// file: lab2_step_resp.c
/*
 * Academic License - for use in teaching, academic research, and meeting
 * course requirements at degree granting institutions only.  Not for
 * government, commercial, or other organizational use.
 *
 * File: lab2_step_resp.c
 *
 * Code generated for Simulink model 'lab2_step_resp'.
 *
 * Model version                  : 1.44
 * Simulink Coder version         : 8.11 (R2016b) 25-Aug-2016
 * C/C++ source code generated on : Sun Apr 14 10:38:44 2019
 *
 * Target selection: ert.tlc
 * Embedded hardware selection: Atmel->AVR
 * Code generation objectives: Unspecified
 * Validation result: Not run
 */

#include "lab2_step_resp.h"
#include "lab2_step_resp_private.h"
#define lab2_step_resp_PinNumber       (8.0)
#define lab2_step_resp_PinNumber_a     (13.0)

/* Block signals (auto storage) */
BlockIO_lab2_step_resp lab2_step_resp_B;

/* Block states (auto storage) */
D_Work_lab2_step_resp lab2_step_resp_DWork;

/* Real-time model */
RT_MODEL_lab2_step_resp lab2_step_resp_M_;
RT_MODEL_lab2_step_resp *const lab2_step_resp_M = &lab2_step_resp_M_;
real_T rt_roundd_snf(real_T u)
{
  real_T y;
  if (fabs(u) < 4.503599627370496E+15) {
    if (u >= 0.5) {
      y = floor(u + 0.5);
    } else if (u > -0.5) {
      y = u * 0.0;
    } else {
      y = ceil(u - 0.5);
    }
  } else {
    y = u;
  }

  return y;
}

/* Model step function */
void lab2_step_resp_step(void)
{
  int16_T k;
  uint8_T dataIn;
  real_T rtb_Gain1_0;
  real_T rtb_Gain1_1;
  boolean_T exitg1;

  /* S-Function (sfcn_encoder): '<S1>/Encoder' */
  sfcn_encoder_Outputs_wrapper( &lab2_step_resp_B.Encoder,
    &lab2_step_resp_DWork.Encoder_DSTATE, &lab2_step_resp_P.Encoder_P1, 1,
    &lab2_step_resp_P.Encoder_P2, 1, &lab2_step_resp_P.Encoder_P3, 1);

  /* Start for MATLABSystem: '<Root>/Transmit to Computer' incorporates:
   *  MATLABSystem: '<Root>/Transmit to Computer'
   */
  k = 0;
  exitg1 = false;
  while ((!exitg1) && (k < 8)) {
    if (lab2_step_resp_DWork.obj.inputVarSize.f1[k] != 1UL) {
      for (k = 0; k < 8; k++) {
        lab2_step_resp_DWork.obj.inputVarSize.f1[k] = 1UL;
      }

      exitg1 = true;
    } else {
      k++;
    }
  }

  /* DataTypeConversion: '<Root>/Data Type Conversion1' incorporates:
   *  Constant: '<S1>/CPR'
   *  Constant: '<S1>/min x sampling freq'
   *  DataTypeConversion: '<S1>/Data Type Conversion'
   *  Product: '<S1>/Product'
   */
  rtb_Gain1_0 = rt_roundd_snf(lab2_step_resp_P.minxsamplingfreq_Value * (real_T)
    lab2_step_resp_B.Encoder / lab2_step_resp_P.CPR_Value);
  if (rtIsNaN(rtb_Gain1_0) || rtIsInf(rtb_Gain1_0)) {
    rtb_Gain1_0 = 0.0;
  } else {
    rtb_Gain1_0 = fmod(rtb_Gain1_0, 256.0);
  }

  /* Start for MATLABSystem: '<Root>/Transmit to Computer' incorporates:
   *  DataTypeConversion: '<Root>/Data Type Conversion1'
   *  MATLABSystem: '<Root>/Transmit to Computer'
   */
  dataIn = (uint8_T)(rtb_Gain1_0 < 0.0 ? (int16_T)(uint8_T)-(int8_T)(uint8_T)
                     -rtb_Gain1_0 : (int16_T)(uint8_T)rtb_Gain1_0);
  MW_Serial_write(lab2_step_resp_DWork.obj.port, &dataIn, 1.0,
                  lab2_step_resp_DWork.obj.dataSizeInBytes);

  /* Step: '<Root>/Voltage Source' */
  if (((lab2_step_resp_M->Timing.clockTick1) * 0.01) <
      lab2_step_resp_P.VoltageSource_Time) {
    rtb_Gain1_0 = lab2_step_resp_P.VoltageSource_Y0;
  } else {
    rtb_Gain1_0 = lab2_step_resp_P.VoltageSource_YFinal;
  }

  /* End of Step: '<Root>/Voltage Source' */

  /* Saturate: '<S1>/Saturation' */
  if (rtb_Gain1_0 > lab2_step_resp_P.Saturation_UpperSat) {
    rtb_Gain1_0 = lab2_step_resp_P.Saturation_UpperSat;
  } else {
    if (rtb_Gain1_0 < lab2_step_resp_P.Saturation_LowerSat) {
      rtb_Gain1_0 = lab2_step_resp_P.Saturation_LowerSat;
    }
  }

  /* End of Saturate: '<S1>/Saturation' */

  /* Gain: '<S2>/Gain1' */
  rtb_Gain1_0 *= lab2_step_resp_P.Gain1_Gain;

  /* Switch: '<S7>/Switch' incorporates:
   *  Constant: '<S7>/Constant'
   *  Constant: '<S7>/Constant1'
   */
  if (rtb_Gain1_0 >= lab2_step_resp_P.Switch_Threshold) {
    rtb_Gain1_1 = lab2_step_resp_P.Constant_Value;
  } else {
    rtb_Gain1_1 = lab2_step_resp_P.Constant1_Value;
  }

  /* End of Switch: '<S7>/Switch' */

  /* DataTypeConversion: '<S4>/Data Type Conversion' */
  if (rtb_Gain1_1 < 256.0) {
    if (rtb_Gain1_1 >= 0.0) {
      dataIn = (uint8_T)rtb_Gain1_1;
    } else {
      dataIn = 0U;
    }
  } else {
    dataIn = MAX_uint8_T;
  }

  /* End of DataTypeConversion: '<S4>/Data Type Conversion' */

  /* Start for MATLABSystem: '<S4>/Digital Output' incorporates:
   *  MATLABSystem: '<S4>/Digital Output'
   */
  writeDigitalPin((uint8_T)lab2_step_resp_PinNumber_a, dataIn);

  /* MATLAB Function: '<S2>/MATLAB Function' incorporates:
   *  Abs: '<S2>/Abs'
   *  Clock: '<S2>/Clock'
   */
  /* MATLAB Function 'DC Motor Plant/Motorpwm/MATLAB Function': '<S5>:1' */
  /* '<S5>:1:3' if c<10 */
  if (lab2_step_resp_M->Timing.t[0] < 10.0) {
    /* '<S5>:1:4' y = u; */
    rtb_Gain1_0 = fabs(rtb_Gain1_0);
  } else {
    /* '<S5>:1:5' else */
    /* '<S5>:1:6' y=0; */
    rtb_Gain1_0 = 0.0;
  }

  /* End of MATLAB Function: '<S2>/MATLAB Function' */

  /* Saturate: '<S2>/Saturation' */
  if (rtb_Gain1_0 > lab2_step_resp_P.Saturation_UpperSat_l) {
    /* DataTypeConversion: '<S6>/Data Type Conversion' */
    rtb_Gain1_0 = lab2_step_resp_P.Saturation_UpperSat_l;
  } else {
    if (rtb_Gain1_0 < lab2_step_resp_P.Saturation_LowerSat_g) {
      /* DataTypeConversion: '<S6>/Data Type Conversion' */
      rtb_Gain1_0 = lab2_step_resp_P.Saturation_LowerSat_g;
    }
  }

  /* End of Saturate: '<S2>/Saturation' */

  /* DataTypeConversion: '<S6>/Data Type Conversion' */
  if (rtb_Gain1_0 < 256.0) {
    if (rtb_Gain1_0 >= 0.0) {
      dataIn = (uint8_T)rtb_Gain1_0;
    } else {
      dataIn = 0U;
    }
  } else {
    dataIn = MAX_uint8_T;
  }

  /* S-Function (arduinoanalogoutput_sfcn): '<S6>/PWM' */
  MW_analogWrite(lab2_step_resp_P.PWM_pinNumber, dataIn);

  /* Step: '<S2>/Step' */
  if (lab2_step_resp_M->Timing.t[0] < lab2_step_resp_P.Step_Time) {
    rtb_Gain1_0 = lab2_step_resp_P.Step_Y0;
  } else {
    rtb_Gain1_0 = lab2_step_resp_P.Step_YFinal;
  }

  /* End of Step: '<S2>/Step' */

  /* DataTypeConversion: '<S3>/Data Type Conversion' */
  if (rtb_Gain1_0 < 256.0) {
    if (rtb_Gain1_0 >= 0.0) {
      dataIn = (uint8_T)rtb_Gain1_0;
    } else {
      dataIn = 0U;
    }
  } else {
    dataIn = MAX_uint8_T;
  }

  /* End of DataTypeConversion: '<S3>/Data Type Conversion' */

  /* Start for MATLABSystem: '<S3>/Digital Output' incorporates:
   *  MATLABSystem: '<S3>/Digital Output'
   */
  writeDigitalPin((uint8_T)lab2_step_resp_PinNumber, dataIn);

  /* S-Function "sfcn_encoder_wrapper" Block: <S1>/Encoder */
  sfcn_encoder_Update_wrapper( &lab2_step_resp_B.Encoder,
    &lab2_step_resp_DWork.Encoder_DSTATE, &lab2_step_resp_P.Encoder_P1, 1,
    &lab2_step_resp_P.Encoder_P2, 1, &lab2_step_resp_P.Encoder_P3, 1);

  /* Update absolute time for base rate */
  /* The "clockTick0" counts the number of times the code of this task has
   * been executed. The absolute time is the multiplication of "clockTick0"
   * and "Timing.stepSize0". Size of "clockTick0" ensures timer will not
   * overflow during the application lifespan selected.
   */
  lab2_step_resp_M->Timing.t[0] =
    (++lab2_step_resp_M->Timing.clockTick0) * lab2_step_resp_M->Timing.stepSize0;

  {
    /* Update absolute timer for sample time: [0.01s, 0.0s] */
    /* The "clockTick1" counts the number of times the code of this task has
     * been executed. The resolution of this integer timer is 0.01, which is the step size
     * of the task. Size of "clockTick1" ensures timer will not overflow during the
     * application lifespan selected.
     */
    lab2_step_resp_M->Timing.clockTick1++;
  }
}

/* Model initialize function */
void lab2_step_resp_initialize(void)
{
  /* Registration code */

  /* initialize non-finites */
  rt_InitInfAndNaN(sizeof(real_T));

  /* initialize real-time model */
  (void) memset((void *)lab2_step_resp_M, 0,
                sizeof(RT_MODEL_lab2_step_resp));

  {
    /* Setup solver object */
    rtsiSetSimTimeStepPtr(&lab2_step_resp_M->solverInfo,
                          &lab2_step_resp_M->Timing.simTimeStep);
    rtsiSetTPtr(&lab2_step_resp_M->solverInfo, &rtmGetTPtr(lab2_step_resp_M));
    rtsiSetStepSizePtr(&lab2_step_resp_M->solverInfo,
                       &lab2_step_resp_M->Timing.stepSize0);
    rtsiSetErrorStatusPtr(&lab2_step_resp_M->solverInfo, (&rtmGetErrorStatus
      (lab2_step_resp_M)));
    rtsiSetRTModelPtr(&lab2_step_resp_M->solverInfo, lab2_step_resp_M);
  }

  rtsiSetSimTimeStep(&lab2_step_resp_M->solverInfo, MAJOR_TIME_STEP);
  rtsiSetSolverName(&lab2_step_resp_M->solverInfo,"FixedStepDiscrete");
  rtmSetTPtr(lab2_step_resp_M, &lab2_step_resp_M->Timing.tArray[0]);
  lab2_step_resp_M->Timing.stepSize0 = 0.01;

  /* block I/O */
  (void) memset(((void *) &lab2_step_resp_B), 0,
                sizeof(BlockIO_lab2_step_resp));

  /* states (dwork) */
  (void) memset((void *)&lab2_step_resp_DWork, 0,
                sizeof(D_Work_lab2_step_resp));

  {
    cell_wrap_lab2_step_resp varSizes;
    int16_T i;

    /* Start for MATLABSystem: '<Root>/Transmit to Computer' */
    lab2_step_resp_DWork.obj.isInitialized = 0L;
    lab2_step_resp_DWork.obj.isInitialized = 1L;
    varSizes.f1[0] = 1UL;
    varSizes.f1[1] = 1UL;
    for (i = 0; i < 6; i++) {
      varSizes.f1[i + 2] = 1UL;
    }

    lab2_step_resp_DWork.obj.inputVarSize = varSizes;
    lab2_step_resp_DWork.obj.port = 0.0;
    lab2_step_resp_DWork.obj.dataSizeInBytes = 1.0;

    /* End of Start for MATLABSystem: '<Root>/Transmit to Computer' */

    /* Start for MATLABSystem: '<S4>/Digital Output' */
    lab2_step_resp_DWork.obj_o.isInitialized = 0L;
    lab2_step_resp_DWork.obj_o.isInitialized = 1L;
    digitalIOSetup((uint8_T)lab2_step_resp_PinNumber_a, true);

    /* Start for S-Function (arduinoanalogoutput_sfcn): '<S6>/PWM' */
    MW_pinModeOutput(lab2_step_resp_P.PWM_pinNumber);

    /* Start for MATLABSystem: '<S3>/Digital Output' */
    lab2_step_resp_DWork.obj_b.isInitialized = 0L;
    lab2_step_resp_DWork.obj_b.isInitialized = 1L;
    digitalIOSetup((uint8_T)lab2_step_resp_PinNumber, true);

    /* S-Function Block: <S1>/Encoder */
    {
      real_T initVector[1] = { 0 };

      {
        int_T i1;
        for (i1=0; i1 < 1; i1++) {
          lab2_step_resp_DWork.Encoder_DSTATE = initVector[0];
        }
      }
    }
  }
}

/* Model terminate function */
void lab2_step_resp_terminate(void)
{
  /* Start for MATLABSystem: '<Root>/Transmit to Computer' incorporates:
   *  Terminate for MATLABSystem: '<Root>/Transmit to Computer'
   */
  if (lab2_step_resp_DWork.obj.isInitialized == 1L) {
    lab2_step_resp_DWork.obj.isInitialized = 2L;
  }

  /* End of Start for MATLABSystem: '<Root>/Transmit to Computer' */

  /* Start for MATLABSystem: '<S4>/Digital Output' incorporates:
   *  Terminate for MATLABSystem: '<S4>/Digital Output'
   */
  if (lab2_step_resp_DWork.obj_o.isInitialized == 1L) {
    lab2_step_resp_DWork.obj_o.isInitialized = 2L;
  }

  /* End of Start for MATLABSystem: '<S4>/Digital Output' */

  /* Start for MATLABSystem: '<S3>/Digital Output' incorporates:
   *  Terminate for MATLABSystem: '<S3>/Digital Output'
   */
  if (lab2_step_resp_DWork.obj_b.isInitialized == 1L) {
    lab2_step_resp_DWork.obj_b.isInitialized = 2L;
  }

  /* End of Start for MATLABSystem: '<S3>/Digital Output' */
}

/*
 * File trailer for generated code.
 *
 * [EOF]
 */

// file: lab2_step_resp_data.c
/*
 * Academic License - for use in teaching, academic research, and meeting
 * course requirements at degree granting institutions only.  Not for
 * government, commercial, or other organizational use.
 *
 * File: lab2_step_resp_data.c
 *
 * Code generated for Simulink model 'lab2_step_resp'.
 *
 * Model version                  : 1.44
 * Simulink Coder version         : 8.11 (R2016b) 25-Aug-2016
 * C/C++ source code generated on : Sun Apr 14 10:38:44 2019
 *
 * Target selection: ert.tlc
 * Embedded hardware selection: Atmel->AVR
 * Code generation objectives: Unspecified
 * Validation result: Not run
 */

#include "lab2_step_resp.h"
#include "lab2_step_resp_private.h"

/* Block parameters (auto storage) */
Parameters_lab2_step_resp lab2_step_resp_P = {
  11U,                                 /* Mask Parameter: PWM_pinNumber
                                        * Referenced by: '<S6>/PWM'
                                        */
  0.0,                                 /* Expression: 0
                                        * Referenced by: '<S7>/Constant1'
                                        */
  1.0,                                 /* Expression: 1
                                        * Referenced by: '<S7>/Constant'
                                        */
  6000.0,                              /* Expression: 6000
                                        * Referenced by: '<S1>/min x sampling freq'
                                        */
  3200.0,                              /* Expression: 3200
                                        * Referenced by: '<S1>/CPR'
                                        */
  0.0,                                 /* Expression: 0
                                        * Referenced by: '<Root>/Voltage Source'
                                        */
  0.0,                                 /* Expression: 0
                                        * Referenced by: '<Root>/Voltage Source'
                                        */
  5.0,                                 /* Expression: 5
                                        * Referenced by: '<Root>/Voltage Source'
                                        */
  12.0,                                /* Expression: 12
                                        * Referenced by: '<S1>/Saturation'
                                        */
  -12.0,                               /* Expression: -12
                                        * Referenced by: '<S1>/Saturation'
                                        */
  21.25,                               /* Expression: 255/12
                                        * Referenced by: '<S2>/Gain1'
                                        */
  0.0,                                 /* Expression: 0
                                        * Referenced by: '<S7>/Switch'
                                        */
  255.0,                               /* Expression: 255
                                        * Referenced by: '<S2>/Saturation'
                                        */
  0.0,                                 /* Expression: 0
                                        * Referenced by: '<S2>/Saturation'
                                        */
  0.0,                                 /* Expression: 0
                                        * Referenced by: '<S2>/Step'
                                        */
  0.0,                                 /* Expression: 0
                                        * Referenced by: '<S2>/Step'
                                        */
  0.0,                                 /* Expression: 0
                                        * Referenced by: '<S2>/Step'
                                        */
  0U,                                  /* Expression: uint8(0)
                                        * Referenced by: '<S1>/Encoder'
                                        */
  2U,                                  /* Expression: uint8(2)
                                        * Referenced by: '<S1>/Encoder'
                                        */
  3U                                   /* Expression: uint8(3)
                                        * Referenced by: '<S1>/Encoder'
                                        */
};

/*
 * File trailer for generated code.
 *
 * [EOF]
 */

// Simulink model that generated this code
simulink model "lab2_step_resp"  (R2016b)
settings: Solver=ode3  StartTime=0.0  StopTime=10  FixedStep=0.01  RelTol=1e-3
libraries: arduinolib x4, neural x1

== system lab2_step_resp ==
  DC Motor Plant : Subsystem
  Data Type Conversion1 : DataTypeConversion  OutDataTypeStr=uint8  RndMeth=Round
  Transmit to Computer : arduinolib/Serial Transmit  portNumber=0  blockPlatform=arduino
  Voltage Source : Step  Time=0  After=5  SampleTime=0.01
  wires:
  Data Type Conversion1/1 -> Transmit to Computer/1
  Voltage Source/1 -> DC Motor Plant/1(Voltage (V))
  DC Motor Plant/1(Velocity (rpm)) -> Data Type Conversion1/1

== system lab2_step_resp/DC Motor Plant ==
  Voltage (V) : Inport
  CPR : Constant  Value=3200
  Data Type Conversion : DataTypeConversion  OutDataTypeStr=double  RndMeth=Round
  Encoder : S-Function  InitFcn=try, set_param(gcb,'FunctionName','sfcn_encoder'), end  FunctionName=sfcn_encoder  Parameters=uint8(0),uint8(2),uint8(3)  SFunctionModules=sfcn_encoder_wrapper  SFunctionDeploymentMode=off  EnableBusSupport=off  mask(S-Function Builder){}
      mask init:
      | val = [[.9  0.75 0.75 1 1 .9 .9 1]',[1 1 0.75 0.75 .9 .9 1 .9]'];try , sys = get_param(gcb,'SfunBuilderFcnName');if isempty(sys), sys = get_param(gcb,'FunctionName'); end,catch, sys = get_param(gcb,'FunctionName'); end
  Motorpwm : Subsystem
  Product : Product  Inputs=**/
  Saturation : Saturate  UpperLimit=12  LowerLimit=-12
  min x sampling freq : Constant  Value=6000
  Velocity (rpm) : Outport
  wires:
  Encoder/1 -> Data Type Conversion/1
  Voltage (V)/1 -> Saturation/1
  Data Type Conversion/1 -> Product/2
  Product/1 -> Velocity (rpm)/1
  min x sampling freq/1 -> Product/1
  CPR/1 -> Product/3
  Saturation/1 -> Motorpwm/1(In1)

== system lab2_step_resp/DC Motor Plant/Motorpwm ==
  In1 : Inport
  Abs : Abs
  Brake : arduinolib/Digital Output  pinNumber=8  blockPlatform=arduino
  Clock : Clock
  "Direction " : arduinolib/Digital Output  pinNumber=13  blockPlatform=arduino
  Gain1 : Gain  Gain=255/12
  MATLAB Function : MATLAB Function  TreatAsAtomicUnit=on
  PWM : arduinolib/PWM  pinNumber=11  blockPlatform=arduino
  Saturation : Saturate  UpperLimit=255  LowerLimit=0
  Step : Step  Time=0  After=0  SampleTime=0
  hardlim : neural/Transfer Functions/hardlim
  wires:
  hardlim/1 -> "Direction "/1
  Step/1 -> Brake/1
  Saturation/1 -> PWM/1
  In1/1 -> Gain1/1
  MATLAB Function/1(y) -> Saturation/1
  Abs/1 -> MATLAB Function/1(u)
  Clock/1 -> MATLAB Function/2(c)
  Gain1/1 -> hardlim/1, Abs/1

== matlab function lab2_step_resp/DC Motor Plant/Motorpwm/MATLAB Function ==
function y = fcn(u,c)
%#codegen
if c<10
    y = u;
else
    y=0;
end
